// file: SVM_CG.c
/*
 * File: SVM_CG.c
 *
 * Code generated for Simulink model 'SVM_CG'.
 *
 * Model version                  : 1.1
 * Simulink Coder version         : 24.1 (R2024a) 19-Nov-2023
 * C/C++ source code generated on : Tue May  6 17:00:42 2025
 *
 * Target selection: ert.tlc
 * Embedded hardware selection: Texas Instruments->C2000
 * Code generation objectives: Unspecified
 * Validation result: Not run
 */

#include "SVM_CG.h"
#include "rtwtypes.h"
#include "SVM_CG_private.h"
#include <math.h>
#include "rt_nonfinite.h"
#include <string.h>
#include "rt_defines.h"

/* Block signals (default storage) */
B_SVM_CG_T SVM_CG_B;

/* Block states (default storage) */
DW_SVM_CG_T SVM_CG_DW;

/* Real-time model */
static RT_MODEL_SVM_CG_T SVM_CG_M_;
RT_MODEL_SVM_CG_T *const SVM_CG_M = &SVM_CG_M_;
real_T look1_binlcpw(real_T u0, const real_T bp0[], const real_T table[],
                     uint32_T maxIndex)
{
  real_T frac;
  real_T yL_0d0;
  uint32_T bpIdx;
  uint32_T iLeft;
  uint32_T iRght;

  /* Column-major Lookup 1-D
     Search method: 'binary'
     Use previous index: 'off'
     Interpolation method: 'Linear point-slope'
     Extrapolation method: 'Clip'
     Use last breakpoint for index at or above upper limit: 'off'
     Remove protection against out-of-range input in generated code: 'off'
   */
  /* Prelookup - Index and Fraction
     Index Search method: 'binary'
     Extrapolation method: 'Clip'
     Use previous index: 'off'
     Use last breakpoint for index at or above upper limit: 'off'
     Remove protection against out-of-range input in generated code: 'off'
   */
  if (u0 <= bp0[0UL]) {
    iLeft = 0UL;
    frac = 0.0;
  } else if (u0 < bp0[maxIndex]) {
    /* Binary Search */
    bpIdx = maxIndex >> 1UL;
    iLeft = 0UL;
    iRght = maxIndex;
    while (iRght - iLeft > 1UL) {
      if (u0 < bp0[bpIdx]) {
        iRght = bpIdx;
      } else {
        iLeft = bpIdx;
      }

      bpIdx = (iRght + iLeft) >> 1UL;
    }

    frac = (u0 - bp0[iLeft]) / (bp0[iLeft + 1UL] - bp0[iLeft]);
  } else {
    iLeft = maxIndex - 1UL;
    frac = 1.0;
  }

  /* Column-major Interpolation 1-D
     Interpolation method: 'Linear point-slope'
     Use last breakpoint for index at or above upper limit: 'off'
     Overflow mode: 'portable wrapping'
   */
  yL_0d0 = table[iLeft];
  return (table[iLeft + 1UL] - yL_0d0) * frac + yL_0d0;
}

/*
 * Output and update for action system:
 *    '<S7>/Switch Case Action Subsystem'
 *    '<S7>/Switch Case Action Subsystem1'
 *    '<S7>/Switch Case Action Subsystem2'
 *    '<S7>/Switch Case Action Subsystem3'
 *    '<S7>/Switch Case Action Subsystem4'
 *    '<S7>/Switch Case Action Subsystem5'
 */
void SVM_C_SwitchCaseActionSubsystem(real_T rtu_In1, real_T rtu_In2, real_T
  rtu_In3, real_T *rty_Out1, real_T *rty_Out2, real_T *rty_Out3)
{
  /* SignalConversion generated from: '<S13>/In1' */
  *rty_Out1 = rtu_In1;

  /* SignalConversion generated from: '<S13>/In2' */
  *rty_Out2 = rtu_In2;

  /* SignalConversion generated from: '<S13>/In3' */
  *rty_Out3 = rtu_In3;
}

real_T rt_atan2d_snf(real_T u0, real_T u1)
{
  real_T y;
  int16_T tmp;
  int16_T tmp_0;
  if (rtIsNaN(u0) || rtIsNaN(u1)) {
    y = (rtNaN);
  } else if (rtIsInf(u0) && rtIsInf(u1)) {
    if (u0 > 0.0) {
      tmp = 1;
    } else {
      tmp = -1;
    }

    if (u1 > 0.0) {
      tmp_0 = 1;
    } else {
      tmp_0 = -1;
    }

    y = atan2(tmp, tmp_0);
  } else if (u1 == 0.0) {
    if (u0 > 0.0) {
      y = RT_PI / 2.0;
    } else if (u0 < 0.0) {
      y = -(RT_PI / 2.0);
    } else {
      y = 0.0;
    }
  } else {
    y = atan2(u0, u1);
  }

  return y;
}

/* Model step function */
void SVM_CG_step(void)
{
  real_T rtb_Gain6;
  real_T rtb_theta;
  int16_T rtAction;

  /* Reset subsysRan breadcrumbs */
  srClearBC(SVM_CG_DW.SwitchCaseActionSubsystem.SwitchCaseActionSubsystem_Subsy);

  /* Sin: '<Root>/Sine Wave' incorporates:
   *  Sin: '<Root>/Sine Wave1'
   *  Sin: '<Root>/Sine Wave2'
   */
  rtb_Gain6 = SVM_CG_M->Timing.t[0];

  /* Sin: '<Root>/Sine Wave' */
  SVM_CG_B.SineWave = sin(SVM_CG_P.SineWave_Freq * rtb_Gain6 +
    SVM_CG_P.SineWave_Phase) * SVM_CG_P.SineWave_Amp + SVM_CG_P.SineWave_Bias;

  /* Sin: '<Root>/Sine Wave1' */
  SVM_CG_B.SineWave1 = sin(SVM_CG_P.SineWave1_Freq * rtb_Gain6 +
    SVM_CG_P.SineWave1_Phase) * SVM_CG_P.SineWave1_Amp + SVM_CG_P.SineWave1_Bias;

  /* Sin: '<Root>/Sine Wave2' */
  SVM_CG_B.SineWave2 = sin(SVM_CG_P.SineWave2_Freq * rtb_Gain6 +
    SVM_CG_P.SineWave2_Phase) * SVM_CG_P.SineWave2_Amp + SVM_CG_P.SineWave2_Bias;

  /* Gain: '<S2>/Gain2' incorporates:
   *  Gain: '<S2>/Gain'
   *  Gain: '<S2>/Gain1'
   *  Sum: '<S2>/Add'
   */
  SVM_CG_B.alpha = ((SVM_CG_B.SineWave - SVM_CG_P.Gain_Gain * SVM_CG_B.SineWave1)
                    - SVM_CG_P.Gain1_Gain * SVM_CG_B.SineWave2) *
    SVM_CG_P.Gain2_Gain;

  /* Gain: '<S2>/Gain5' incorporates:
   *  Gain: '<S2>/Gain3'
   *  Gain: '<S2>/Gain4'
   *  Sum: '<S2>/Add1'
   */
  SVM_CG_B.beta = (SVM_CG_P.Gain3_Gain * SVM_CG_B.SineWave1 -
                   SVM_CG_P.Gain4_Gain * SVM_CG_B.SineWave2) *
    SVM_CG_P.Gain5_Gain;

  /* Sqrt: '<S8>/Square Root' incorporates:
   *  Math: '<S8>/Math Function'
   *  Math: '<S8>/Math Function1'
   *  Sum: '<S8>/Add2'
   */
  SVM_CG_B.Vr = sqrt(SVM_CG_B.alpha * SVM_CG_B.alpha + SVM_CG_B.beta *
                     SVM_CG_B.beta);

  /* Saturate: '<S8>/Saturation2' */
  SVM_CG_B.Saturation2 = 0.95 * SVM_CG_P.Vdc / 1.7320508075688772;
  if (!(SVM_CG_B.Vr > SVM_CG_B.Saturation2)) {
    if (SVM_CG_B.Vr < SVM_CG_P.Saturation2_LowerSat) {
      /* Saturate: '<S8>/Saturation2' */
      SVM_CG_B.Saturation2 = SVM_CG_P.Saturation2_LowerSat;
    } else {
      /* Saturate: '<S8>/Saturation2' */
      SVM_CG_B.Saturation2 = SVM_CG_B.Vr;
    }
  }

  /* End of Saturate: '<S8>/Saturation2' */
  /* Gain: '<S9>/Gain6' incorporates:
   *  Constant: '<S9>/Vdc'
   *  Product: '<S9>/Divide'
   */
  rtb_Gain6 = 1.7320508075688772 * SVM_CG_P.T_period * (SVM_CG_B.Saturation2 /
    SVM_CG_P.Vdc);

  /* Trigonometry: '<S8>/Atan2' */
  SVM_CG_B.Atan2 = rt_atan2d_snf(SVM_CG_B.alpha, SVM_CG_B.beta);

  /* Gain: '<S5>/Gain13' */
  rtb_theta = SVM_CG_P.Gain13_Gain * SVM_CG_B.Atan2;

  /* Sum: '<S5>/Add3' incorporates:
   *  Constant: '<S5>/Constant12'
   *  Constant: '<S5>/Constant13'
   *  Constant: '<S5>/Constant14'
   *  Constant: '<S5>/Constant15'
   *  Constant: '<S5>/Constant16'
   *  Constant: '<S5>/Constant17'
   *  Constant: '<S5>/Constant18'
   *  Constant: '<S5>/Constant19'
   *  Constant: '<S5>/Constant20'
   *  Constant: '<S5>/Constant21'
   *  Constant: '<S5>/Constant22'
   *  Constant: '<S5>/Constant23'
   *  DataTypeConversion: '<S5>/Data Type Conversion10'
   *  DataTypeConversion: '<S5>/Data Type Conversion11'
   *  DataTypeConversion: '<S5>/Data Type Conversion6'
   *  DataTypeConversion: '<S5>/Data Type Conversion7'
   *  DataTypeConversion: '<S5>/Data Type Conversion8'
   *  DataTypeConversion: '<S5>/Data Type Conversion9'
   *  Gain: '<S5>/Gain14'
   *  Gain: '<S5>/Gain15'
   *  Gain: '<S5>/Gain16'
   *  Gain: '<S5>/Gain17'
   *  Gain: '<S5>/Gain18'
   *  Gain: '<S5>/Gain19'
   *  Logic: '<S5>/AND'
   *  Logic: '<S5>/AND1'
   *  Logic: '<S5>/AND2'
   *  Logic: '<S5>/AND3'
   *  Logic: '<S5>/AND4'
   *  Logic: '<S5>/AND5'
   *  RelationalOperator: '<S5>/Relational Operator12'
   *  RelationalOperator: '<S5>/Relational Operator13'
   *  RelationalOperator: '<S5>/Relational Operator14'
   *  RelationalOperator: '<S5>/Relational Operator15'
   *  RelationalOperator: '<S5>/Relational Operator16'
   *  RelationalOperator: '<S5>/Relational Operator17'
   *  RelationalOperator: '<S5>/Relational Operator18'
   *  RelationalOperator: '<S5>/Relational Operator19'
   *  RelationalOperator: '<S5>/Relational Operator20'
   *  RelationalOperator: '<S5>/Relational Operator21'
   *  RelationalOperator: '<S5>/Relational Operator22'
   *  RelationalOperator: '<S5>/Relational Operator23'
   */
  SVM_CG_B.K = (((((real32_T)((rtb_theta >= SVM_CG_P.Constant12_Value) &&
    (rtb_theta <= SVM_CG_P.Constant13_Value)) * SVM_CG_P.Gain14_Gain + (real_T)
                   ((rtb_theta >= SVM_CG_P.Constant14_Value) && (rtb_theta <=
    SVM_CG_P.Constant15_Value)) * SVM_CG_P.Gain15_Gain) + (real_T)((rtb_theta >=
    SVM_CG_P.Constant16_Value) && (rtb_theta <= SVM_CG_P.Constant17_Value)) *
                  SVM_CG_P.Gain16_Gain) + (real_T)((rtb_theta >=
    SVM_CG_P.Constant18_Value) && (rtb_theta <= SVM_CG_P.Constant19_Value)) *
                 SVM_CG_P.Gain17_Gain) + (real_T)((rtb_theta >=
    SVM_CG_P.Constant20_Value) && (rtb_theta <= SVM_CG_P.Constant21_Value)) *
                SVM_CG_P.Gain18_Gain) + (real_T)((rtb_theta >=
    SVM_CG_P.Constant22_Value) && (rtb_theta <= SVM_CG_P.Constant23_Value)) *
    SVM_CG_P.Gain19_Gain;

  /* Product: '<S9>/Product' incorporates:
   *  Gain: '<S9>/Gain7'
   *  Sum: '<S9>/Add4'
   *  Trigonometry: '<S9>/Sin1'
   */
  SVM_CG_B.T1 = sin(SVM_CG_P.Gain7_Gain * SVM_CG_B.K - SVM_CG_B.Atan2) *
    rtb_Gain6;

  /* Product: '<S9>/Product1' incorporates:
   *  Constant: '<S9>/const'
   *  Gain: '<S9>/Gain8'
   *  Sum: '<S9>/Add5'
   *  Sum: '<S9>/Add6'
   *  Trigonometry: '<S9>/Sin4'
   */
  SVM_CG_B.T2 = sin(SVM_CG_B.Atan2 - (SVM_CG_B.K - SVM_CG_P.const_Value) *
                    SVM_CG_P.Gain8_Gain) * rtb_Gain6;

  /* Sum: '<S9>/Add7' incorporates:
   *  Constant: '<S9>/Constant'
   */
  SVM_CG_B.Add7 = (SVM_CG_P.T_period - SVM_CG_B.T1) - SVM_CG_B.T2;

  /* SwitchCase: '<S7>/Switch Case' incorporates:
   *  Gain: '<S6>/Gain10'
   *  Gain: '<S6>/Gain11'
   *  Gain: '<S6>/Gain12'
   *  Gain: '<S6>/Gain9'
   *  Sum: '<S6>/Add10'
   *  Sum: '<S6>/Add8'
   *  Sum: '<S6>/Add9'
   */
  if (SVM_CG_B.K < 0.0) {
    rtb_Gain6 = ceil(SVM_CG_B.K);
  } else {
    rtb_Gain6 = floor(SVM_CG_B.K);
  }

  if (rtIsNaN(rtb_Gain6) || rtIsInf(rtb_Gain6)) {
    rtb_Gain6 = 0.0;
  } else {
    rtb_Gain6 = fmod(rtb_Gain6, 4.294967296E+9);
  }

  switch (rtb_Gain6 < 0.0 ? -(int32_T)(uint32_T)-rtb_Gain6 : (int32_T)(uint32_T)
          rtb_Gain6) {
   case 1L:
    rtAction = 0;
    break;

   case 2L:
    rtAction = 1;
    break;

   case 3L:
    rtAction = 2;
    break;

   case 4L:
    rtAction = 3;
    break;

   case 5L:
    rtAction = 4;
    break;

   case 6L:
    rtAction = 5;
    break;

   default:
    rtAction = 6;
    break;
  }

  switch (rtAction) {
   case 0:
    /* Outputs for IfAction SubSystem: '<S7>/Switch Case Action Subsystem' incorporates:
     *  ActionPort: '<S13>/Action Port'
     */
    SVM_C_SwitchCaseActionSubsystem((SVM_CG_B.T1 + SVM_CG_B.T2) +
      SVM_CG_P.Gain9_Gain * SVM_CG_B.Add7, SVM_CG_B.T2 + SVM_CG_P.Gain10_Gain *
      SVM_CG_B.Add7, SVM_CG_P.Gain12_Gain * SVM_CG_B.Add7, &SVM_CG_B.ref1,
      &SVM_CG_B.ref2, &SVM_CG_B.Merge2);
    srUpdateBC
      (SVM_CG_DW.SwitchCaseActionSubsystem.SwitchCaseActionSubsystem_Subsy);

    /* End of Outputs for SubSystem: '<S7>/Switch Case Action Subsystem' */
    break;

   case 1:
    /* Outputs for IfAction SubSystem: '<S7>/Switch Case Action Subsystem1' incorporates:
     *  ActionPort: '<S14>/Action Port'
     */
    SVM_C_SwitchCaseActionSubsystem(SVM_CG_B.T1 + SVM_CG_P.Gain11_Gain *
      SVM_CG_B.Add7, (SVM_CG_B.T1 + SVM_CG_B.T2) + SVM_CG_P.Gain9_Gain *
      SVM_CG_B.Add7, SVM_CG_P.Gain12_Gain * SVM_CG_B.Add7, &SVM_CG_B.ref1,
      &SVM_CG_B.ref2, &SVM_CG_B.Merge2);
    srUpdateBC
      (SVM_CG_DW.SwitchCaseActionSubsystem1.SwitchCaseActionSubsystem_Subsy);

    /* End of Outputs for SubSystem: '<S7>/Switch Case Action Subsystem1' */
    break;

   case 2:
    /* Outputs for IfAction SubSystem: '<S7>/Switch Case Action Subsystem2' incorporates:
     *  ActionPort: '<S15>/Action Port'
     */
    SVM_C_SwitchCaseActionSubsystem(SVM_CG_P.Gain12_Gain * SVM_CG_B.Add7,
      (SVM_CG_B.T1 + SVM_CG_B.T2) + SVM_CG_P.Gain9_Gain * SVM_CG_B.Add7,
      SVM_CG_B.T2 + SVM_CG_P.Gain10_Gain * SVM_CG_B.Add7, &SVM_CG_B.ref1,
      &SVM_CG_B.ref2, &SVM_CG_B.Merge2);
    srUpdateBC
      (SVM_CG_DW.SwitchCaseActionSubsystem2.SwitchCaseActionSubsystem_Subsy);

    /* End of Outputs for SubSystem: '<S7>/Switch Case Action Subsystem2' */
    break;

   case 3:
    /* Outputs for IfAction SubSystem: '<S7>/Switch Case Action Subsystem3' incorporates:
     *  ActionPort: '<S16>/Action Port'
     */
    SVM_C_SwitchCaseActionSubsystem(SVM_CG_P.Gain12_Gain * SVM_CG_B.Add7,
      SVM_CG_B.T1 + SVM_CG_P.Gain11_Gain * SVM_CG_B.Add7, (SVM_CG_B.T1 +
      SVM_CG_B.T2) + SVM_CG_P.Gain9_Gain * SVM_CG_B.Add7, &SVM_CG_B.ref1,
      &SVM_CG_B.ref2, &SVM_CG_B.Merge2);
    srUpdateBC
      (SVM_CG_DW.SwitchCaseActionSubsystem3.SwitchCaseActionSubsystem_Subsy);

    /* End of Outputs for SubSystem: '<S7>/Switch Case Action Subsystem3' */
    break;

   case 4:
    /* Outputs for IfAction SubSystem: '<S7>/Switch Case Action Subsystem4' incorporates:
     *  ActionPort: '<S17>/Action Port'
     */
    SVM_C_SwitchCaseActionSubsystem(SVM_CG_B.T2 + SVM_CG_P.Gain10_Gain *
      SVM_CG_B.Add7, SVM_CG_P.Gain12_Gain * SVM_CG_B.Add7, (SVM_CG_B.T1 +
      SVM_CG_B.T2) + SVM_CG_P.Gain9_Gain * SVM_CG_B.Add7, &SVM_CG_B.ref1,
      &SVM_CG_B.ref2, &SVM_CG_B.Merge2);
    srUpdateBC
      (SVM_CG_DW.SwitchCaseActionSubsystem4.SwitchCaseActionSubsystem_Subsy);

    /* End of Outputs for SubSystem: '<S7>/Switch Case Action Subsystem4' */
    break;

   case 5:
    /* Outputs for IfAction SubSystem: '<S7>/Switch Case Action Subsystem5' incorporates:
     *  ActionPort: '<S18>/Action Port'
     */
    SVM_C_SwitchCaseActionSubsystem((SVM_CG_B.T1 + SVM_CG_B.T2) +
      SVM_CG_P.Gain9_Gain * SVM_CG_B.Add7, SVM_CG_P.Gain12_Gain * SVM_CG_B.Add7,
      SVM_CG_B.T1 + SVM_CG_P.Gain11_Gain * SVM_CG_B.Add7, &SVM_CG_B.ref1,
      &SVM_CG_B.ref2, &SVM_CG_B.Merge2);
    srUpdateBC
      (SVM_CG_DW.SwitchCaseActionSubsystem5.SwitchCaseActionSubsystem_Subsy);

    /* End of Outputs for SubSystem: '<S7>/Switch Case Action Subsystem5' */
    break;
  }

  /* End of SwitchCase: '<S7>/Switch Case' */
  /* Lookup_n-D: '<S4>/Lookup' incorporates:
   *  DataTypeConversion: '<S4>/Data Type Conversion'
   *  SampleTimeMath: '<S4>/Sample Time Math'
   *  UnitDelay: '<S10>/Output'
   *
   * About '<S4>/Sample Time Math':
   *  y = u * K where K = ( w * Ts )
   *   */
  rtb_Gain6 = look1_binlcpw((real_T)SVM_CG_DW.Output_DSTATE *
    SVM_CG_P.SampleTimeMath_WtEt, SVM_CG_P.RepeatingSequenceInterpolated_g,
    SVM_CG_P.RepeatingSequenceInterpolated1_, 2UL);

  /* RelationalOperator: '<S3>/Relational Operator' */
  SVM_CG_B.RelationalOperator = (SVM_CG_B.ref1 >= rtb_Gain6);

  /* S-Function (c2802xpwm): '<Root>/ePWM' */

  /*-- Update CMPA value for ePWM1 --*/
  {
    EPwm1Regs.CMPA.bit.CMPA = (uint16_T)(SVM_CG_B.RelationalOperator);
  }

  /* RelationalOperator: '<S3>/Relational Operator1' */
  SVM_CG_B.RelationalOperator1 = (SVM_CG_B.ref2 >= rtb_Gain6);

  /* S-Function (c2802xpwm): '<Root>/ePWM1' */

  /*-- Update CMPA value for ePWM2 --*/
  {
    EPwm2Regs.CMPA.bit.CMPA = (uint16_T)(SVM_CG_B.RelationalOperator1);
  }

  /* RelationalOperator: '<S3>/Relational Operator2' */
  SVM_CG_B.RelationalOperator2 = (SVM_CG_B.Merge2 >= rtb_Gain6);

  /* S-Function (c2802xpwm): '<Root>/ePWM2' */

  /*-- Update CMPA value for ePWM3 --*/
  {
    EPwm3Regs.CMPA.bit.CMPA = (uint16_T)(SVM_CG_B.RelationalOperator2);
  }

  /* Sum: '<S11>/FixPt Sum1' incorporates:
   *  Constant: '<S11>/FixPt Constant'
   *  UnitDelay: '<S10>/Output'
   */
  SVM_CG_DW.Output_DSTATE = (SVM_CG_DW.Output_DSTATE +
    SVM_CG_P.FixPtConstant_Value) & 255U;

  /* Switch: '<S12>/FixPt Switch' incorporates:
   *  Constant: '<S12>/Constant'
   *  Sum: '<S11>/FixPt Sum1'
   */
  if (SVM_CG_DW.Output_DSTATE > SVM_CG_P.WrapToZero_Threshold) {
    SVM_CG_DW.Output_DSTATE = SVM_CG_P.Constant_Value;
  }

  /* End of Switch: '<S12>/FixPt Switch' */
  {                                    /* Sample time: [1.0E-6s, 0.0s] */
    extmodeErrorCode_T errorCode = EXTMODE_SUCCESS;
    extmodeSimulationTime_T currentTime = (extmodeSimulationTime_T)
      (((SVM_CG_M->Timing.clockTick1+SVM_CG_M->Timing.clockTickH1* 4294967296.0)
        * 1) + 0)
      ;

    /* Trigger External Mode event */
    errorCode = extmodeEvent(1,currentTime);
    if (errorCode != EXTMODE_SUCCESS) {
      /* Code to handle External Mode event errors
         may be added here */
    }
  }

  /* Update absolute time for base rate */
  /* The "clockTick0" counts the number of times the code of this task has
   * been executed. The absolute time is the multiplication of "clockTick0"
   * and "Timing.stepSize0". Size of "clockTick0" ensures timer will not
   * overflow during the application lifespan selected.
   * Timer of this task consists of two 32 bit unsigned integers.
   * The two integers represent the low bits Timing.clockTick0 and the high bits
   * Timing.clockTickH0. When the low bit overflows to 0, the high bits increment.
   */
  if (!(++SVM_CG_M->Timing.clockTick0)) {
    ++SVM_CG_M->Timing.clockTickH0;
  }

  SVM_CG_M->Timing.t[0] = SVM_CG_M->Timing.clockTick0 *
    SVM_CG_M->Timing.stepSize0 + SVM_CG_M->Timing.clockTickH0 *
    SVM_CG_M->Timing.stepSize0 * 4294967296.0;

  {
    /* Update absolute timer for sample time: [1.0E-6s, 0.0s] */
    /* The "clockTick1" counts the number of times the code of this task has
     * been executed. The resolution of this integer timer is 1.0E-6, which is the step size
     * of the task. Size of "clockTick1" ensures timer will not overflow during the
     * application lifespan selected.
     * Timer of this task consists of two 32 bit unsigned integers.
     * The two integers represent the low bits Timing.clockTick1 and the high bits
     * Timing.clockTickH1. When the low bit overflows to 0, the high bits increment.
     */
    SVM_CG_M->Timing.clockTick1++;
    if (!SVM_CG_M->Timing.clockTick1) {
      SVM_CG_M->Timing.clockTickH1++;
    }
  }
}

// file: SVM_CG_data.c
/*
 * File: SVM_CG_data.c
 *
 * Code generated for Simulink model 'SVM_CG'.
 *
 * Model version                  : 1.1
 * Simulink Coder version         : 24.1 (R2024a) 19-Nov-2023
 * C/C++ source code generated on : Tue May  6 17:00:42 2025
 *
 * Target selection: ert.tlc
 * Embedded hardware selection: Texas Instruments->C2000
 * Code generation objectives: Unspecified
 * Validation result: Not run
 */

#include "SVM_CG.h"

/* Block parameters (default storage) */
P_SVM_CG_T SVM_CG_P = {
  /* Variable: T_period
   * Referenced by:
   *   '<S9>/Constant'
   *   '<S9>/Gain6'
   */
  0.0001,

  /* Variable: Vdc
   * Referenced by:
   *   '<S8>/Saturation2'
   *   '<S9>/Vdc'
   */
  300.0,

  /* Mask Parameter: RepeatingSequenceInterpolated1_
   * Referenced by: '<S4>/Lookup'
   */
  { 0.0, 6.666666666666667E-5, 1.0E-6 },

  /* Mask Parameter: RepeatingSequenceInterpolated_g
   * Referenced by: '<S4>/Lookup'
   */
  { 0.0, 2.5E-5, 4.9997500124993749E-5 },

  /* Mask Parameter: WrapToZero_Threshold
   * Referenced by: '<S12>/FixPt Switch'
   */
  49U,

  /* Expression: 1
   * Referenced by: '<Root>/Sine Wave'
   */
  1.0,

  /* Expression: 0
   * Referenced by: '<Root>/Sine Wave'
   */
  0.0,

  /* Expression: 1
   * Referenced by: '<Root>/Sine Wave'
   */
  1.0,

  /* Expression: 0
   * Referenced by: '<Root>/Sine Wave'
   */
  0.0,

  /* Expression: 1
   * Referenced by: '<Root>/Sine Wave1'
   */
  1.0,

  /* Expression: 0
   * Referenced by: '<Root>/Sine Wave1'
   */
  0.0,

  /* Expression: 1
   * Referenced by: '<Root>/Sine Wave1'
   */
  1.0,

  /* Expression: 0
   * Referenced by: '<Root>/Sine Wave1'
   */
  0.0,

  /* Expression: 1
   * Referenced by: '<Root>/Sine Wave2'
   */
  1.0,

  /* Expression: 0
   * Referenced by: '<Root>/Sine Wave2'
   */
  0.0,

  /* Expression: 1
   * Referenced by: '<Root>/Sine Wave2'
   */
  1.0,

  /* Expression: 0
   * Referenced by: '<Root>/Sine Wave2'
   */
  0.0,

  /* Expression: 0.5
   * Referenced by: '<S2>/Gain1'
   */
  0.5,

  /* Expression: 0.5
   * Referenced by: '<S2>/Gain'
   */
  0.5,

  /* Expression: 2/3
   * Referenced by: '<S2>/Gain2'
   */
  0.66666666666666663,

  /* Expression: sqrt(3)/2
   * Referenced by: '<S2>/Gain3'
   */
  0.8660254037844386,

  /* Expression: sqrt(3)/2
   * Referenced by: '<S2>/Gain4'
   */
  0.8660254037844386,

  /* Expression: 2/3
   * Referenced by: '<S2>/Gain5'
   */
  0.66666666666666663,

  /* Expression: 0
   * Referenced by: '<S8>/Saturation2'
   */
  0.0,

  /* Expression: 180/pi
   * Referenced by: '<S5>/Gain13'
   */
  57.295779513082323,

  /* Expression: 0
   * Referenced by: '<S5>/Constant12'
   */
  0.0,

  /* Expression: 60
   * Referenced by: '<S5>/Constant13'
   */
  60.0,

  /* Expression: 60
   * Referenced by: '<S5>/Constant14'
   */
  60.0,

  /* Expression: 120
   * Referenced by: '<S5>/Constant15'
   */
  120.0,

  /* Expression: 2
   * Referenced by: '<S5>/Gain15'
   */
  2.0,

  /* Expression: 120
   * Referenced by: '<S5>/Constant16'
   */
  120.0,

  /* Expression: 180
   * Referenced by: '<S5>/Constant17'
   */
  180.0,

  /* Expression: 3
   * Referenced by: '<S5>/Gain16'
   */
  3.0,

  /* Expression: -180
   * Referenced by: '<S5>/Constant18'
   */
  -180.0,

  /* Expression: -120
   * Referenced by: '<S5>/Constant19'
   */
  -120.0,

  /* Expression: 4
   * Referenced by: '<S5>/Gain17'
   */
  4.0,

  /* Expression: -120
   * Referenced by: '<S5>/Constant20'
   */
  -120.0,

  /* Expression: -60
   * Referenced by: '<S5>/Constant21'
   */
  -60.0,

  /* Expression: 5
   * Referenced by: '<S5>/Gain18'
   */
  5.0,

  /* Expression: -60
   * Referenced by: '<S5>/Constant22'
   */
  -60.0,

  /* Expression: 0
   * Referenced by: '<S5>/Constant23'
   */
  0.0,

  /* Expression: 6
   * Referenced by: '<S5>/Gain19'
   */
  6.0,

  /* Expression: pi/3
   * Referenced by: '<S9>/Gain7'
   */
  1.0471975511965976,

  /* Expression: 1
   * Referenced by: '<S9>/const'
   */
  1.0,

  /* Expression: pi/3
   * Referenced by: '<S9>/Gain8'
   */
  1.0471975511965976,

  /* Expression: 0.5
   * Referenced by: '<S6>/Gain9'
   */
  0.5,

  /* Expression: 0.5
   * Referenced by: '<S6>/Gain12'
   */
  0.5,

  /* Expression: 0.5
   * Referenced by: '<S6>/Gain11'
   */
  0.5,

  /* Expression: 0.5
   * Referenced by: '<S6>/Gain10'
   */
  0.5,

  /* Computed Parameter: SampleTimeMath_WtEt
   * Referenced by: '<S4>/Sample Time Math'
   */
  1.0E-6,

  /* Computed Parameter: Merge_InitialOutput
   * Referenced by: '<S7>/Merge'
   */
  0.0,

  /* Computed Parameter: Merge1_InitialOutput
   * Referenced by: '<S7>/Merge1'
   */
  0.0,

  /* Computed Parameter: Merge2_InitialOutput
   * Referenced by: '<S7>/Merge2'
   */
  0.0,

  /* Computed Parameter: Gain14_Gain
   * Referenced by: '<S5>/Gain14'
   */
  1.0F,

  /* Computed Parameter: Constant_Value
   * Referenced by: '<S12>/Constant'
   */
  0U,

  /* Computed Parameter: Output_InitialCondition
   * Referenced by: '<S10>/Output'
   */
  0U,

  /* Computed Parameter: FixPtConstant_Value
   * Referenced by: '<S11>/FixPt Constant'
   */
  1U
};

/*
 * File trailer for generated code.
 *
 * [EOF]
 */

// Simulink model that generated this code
simulink model "SVM_CG"  (R2024a)
settings: Solver=FixedStepDiscrete  StartTime=0.0  StopTime=Inf  RelTol=1e-3  EnableMultiTasking=on
undefined symbols (not defined in the file): Down, GPTRIP1SEL, T_period, TZ1, Up, Vdc
libraries: c2802xlib x3, simulink x1

== system SVM_CG ==
  SVPWM : Subsystem
  Sine Wave : Sin  SampleTime=0
  Sine Wave1 : Sin  SampleTime=0
  Sine Wave2 : Sin  SampleTime=0
  ePWM : c2802xlib/ePWM  PwmType=C2000_Type4  useModule=ePWM1  ePWMxLINKTBPRD=Not Linked  periodUnits=Clock cycles  timerSource=Specify via dialog  timerPeriod_clk=10000  timerPeriod_sec=0.0001  tbshadow=Counter equals to zero  countingMode=Up-Down  phaseActiveEnable=Disable  phaseDirection=Count down after sync  phaseActive=0  synchronizationEnable=off  dcaevt1Sync=off  dcbevt1Sync=off  synchronizationOption=Disable  dcbevt1SyncOut=off  dcaevt1SyncOut=off  cmpdSyncOut=off  cmpcSyncOut=off  cmpbSyncOut=off  zeroSyncOut=off  swfSyncOut=off  perSynchronizationOption=Counter equals to period (CTR=PRD)  clockPrescale=1  HSclockPrescale=1  enswap=off  ePWMxAStatus=on  ePWMxAactionLogic1=Do nothing  ePWMxAactionLogic2=Do nothing  ePWMxAactionLogic3=Clear  ePWMxAactionLogic4=Set  ePWMxAactionLogic5=Do nothing  ePWMxAactionLogic6=Do nothing  ePWMxACSFenable=off  ePWMxACSFvalue=Forcing disable  ePWMxASFreload=Zero  ePWMxBStatus=on  ePWMxBactionLogic1=Do nothing  ePWMxBactionLogic2=Do nothing  ePWMxBactionLogic3=Set  ePWMxBactionLogic4=Clear  ePWMxBactionLogic5=Do nothing  ePWMxBactionLogic6=Do nothing  ePWMxBCSFenable=off  ePWMxBCSFvalue=Forcing disable  ePWMxBSFreload=Zero  ePWNxBOutWay=off  ePWMxLINKCMPA=Not Linked  CMPAUnits=Clock cycles  CMPASource=Input port  CMPAValue_per=50  CMPAValue_clk=0  enCMPAshadow=Counter equals to zero (CTR=Zero)  ePWMxLINKCMPB=Not Linked  CMPBUnits=Clock cycles  CMPBSource=Specify via dialog  CMPBValue_per=50  CMPBValue_clk=32000  enCMPBshadow=Counter equals to zero (CTR=Zero)  ePWMxLINKCMPC=Not Linked  CMPCUnits=Clock cycles  CMPCSource=Specify via dialog  CMPCValue_per=50  CMPCValue_clk=32000  enCMPCshadow=Counter equals to zero (CTR=Zero)  ePWMxLINKCMPD=Not Linked  CMPDUnits=Clock cycles  CMPDSource=Specify via dialog  CMPDValue_per=50  CMPDValue_clk=32000  enCMPDshadow=Counter equals to zero (CTR=Zero)  enableDBePWMxA=on  enableDBePWMxB=on  enhalfcycle=off  DBpolarity=Active high complementary (AHC)  DBedgeDelay=Positive  DBSource_ePWMxA=ePWMxA  DBSource_ePWMxB=ePWMxA  DBPeriodUnits=Clock cycles  DBperiodSource=Specify via dialog  REDperiod=400  FEDperiod=400  REDperiod_sec=0  FEDperiod_sec=0  LoadModeDBRED=Immediate without using shadow  LoadModeDBFED=Immediate without using shadow  adcstartModuleA=off  adcrequestEventA=First event  adcstartEventA=Digital Compare Module A Event 1 start of conversion (DCAEVT1.soc)  adcstartEventA_type2=Counter equals to zero (CTR=Zero)  adcstartModuleB=off  adcrequestEventB=First event  adcstartEventB=Counter equals to zero (CTR=Zero)  adcstartEventB_type2=Counter equals to zero (CTR=Zero)  intEn=off  intPrd=First event  intSel=Counter equals to zero (CTR=Zero)  intSel_type2=Counter equals to zero (CTR=Zero)  hrpe=off  enHRPWM=off  HRPWM_LoadMode=Counter equals to period (CTR=PRD)  HRPWM_CTLMode=Duty or Period control mode  HRPWM_EDGMode=Both edge  hrpeb=off  enHRPWMB=off  HRPWM_LoadModeB=Counter equals to zero (CTR=ZERO)  HRPWM_CTLModeB=Duty or Period control mode  HRPWM_EDGModeB=Both edge  enHRDBRED=off  enHRDBFED=off  enSFO=on  enautoconv=on  chopperEnable=off  chopperFrequency=1  chopperFirstwidth=1  chopperDuty=12.5%  tripZonesource=Specify via dialog  tzselOSHT1=off  tzselOSHT2=off  tzselOSHT3=off  tzselOSHT4=off  tzselOSHT5=off  tzselOSHT6=off  tzselOSHDCAEV1=off  tzselOSHDCBEV1=off  tzselCBC1=off  tzselCBC2=off  tzselCBC3=off  tzselCBC4=off  tzselCBC5=off  tzselCBC6=off  tzselCBCDCAEV2=off  tzselCBCDCBEV2=off  enTzOstIntr=off  enTzCbcIntr=off  enTzDCAEVT1Intr=off  enTzDCAEVT2Intr=off  enTzDCBEVT1Intr=off  enTzDCBEVT2Intr=off  tzclrCBCLatch=Counter equals to zero (CTR=Zero)  ePWMxAforced=No action  ePWMxBforced=No action  DCAEVT1forced=No action  DCBEVT1forced=No action  DCAEVT2forced=No action  DCBEVT2forced=No action  dcah=Trip Zone 1 input (TZ1)  dcal=Trip Zone 2 input (TZ2)  dcbh=Trip Zone 1 input (TZ1)  dcbl=Trip Zone 2 input (TZ2)  dcah_type2=GPTRIP1SEL/(TZ1)  dcal_type2=GPTRIP1SEL/(TZ1)  dcbh_type2=GPTRIP1SEL/(TZ1)  dcbl_type2=GPTRIP1SEL/(TZ1)  gendcaevt1=Event disabled  gendcaevt2=Event disabled  gendcbevt1=Event disabled  gendcbevt2=Event disabled  dcaevt1src=DCAEVT1 with sync  dcaevt2src=DCAEVT2 with sync  dcbevt1src=DCBEVT1 with sync  dcbevt2src=DCBEVT2 with sync  pulsesel=Counter equals to zero (CTR=Zero)  blankinv=off  blankoffset=0  blankwidth=0  evsrcsel=Filtered version of DCAEVT1 (DCAEVT1FILT)  encape=off
  ePWM1 : c2802xlib/ePWM  PwmType=C2000_Type4  useModule=ePWM2  ePWMxLINKTBPRD=Not Linked  periodUnits=Clock cycles  timerSource=Specify via dialog  timerPeriod_clk=10000  timerPeriod_sec=0.0001  tbshadow=Counter equals to zero  countingMode=Up-Down  phaseActiveEnable=Disable  phaseDirection=Count down after sync  phaseActive=0  synchronizationEnable=off  dcaevt1Sync=off  dcbevt1Sync=off  synchronizationOption=Disable  dcbevt1SyncOut=off  dcaevt1SyncOut=off  cmpdSyncOut=off  cmpcSyncOut=off  cmpbSyncOut=off  zeroSyncOut=off  swfSyncOut=off  perSynchronizationOption=Counter equals to period (CTR=PRD)  clockPrescale=1  HSclockPrescale=1  enswap=off  ePWMxAStatus=on  ePWMxAactionLogic1=Do nothing  ePWMxAactionLogic2=Do nothing  ePWMxAactionLogic3=Clear  ePWMxAactionLogic4=Set  ePWMxAactionLogic5=Do nothing  ePWMxAactionLogic6=Do nothing  ePWMxACSFenable=off  ePWMxACSFvalue=Forcing disable  ePWMxASFreload=Zero  ePWMxBStatus=on  ePWMxBactionLogic1=Do nothing  ePWMxBactionLogic2=Do nothing  ePWMxBactionLogic3=Set  ePWMxBactionLogic4=Clear  ePWMxBactionLogic5=Do nothing  ePWMxBactionLogic6=Do nothing  ePWMxBCSFenable=off  ePWMxBCSFvalue=Forcing disable  ePWMxBSFreload=Zero  ePWNxBOutWay=off  ePWMxLINKCMPA=Not Linked  CMPAUnits=Clock cycles  CMPASource=Input port  CMPAValue_per=50  CMPAValue_clk=0  enCMPAshadow=Counter equals to zero (CTR=Zero)  ePWMxLINKCMPB=Not Linked  CMPBUnits=Clock cycles  CMPBSource=Specify via dialog  CMPBValue_per=50  CMPBValue_clk=32000  enCMPBshadow=Counter equals to zero (CTR=Zero)  ePWMxLINKCMPC=Not Linked  CMPCUnits=Clock cycles  CMPCSource=Specify via dialog  CMPCValue_per=50  CMPCValue_clk=32000  enCMPCshadow=Counter equals to zero (CTR=Zero)  ePWMxLINKCMPD=Not Linked  CMPDUnits=Clock cycles  CMPDSource=Specify via dialog  CMPDValue_per=50  CMPDValue_clk=32000  enCMPDshadow=Counter equals to zero (CTR=Zero)  enableDBePWMxA=on  enableDBePWMxB=on  enhalfcycle=off  DBpolarity=Active high complementary (AHC)  DBedgeDelay=Positive  DBSource_ePWMxA=ePWMxA  DBSource_ePWMxB=ePWMxA  DBPeriodUnits=Clock cycles  DBperiodSource=Specify via dialog  REDperiod=400  FEDperiod=400  REDperiod_sec=0  FEDperiod_sec=0  LoadModeDBRED=Immediate without using shadow  LoadModeDBFED=Immediate without using shadow  adcstartModuleA=off  adcrequestEventA=First event  adcstartEventA=Digital Compare Module A Event 1 start of conversion (DCAEVT1.soc)  adcstartEventA_type2=Counter equals to zero (CTR=Zero)  adcstartModuleB=off  adcrequestEventB=First event  adcstartEventB=Counter equals to zero (CTR=Zero)  adcstartEventB_type2=Counter equals to zero (CTR=Zero)  intEn=off  intPrd=First event  intSel=Counter equals to zero (CTR=Zero)  intSel_type2=Counter equals to zero (CTR=Zero)  hrpe=off  enHRPWM=off  HRPWM_LoadMode=Counter equals to period (CTR=PRD)  HRPWM_CTLMode=Duty or Period control mode  HRPWM_EDGMode=Both edge  hrpeb=off  enHRPWMB=off  HRPWM_LoadModeB=Counter equals to zero (CTR=ZERO)  HRPWM_CTLModeB=Duty or Period control mode  HRPWM_EDGModeB=Both edge  enHRDBRED=off  enHRDBFED=off  enSFO=on  enautoconv=on  chopperEnable=off  chopperFrequency=1  chopperFirstwidth=1  chopperDuty=12.5%  tripZonesource=Specify via dialog  tzselOSHT1=off  tzselOSHT2=off  tzselOSHT3=off  tzselOSHT4=off  tzselOSHT5=off  tzselOSHT6=off  tzselOSHDCAEV1=off  tzselOSHDCBEV1=off  tzselCBC1=off  tzselCBC2=off  tzselCBC3=off  tzselCBC4=off  tzselCBC5=off  tzselCBC6=off  tzselCBCDCAEV2=off  tzselCBCDCBEV2=off  enTzOstIntr=off  enTzCbcIntr=off  enTzDCAEVT1Intr=off  enTzDCAEVT2Intr=off  enTzDCBEVT1Intr=off  enTzDCBEVT2Intr=off  tzclrCBCLatch=Counter equals to zero (CTR=Zero)  ePWMxAforced=No action  ePWMxBforced=No action  DCAEVT1forced=No action  DCBEVT1forced=No action  DCAEVT2forced=No action  DCBEVT2forced=No action  dcah=Trip Zone 1 input (TZ1)  dcal=Trip Zone 2 input (TZ2)  dcbh=Trip Zone 1 input (TZ1)  dcbl=Trip Zone 2 input (TZ2)  dcah_type2=GPTRIP1SEL/(TZ1)  dcal_type2=GPTRIP1SEL/(TZ1)  dcbh_type2=GPTRIP1SEL/(TZ1)  dcbl_type2=GPTRIP1SEL/(TZ1)  gendcaevt1=Event disabled  gendcaevt2=Event disabled  gendcbevt1=Event disabled  gendcbevt2=Event disabled  dcaevt1src=DCAEVT1 with sync  dcaevt2src=DCAEVT2 with sync  dcbevt1src=DCBEVT1 with sync  dcbevt2src=DCBEVT2 with sync  pulsesel=Counter equals to zero (CTR=Zero)  blankinv=off  blankoffset=0  blankwidth=0  evsrcsel=Filtered version of DCAEVT1 (DCAEVT1FILT)  encape=off
  ePWM2 : c2802xlib/ePWM  PwmType=C2000_Type4  useModule=ePWM3  ePWMxLINKTBPRD=Not Linked  periodUnits=Clock cycles  timerSource=Specify via dialog  timerPeriod_clk=10000  timerPeriod_sec=0.0001  tbshadow=Counter equals to zero  countingMode=Up-Down  phaseActiveEnable=Disable  phaseDirection=Count down after sync  phaseActive=0  synchronizationEnable=off  dcaevt1Sync=off  dcbevt1Sync=off  synchronizationOption=Disable  dcbevt1SyncOut=off  dcaevt1SyncOut=off  cmpdSyncOut=off  cmpcSyncOut=off  cmpbSyncOut=off  zeroSyncOut=off  swfSyncOut=off  perSynchronizationOption=Counter equals to period (CTR=PRD)  clockPrescale=1  HSclockPrescale=1  enswap=off  ePWMxAStatus=on  ePWMxAactionLogic1=Do nothing  ePWMxAactionLogic2=Do nothing  ePWMxAactionLogic3=Clear  ePWMxAactionLogic4=Set  ePWMxAactionLogic5=Do nothing  ePWMxAactionLogic6=Do nothing  ePWMxACSFenable=off  ePWMxACSFvalue=Forcing disable  ePWMxASFreload=Zero  ePWMxBStatus=on  ePWMxBactionLogic1=Do nothing  ePWMxBactionLogic2=Do nothing  ePWMxBactionLogic3=Set  ePWMxBactionLogic4=Clear  ePWMxBactionLogic5=Do nothing  ePWMxBactionLogic6=Do nothing  ePWMxBCSFenable=off  ePWMxBCSFvalue=Forcing disable  ePWMxBSFreload=Zero  ePWNxBOutWay=off  ePWMxLINKCMPA=Not Linked  CMPAUnits=Clock cycles  CMPASource=Input port  CMPAValue_per=50  CMPAValue_clk=0  enCMPAshadow=Counter equals to zero (CTR=Zero)  ePWMxLINKCMPB=Not Linked  CMPBUnits=Clock cycles  CMPBSource=Specify via dialog  CMPBValue_per=50  CMPBValue_clk=32000  enCMPBshadow=Counter equals to zero (CTR=Zero)  ePWMxLINKCMPC=Not Linked  CMPCUnits=Clock cycles  CMPCSource=Specify via dialog  CMPCValue_per=50  CMPCValue_clk=32000  enCMPCshadow=Counter equals to zero (CTR=Zero)  ePWMxLINKCMPD=Not Linked  CMPDUnits=Clock cycles  CMPDSource=Specify via dialog  CMPDValue_per=50  CMPDValue_clk=32000  enCMPDshadow=Counter equals to zero (CTR=Zero)  enableDBePWMxA=on  enableDBePWMxB=on  enhalfcycle=off  DBpolarity=Active high complementary (AHC)  DBedgeDelay=Positive  DBSource_ePWMxA=ePWMxA  DBSource_ePWMxB=ePWMxA  DBPeriodUnits=Clock cycles  DBperiodSource=Specify via dialog  REDperiod=400  FEDperiod=400  REDperiod_sec=0  FEDperiod_sec=0  LoadModeDBRED=Immediate without using shadow  LoadModeDBFED=Immediate without using shadow  adcstartModuleA=off  adcrequestEventA=First event  adcstartEventA=Digital Compare Module A Event 1 start of conversion (DCAEVT1.soc)  adcstartEventA_type2=Counter equals to zero (CTR=Zero)  adcstartModuleB=off  adcrequestEventB=First event  adcstartEventB=Counter equals to zero (CTR=Zero)  adcstartEventB_type2=Counter equals to zero (CTR=Zero)  intEn=off  intPrd=First event  intSel=Counter equals to zero (CTR=Zero)  intSel_type2=Counter equals to zero (CTR=Zero)  hrpe=off  enHRPWM=off  HRPWM_LoadMode=Counter equals to period (CTR=PRD)  HRPWM_CTLMode=Duty or Period control mode  HRPWM_EDGMode=Both edge  hrpeb=off  enHRPWMB=off  HRPWM_LoadModeB=Counter equals to zero (CTR=ZERO)  HRPWM_CTLModeB=Duty or Period control mode  HRPWM_EDGModeB=Both edge  enHRDBRED=off  enHRDBFED=off  enSFO=on  enautoconv=on  chopperEnable=off  chopperFrequency=1  chopperFirstwidth=1  chopperDuty=12.5%  tripZonesource=Specify via dialog  tzselOSHT1=off  tzselOSHT2=off  tzselOSHT3=off  tzselOSHT4=off  tzselOSHT5=off  tzselOSHT6=off  tzselOSHDCAEV1=off  tzselOSHDCBEV1=off  tzselCBC1=off  tzselCBC2=off  tzselCBC3=off  tzselCBC4=off  tzselCBC5=off  tzselCBC6=off  tzselCBCDCAEV2=off  tzselCBCDCBEV2=off  enTzOstIntr=off  enTzCbcIntr=off  enTzDCAEVT1Intr=off  enTzDCAEVT2Intr=off  enTzDCBEVT1Intr=off  enTzDCBEVT2Intr=off  tzclrCBCLatch=Counter equals to zero (CTR=Zero)  ePWMxAforced=No action  ePWMxBforced=No action  DCAEVT1forced=No action  DCBEVT1forced=No action  DCAEVT2forced=No action  DCBEVT2forced=No action  dcah=Trip Zone 1 input (TZ1)  dcal=Trip Zone 2 input (TZ2)  dcbh=Trip Zone 1 input (TZ1)  dcbl=Trip Zone 2 input (TZ2)  dcah_type2=GPTRIP1SEL/(TZ1)  dcal_type2=GPTRIP1SEL/(TZ1)  dcbh_type2=GPTRIP1SEL/(TZ1)  dcbl_type2=GPTRIP1SEL/(TZ1)  gendcaevt1=Event disabled  gendcaevt2=Event disabled  gendcbevt1=Event disabled  gendcbevt2=Event disabled  dcaevt1src=DCAEVT1 with sync  dcaevt2src=DCAEVT2 with sync  dcbevt1src=DCBEVT1 with sync  dcbevt2src=DCBEVT2 with sync  pulsesel=Counter equals to zero (CTR=Zero)  blankinv=off  blankoffset=0  blankwidth=0  evsrcsel=Filtered version of DCAEVT1 (DCAEVT1FILT)  encape=off
  wires:
  Sine Wave2/1 -> SVPWM/3(Vc)
  Sine Wave1/1 -> SVPWM/2(Vb)
  Sine Wave/1 -> SVPWM/1(Va)
  SVPWM/3(T5) -> ePWM2/1
  SVPWM/2(T3) -> ePWM1/1
  SVPWM/1(T1) -> ePWM/1

== system SVM_CG/SVPWM ==
  Va : Inport
  Vb : Inport  Port=2
  Vc : Inport  Port=3
  ABC to alpha-beta : Subsystem
  Goto6 : Goto  TagVisibility=global
  PWM : Subsystem
  Repeating Sequence Interpolated1 : simulink/Sources/Repeating Sequence Interpolated  OutValues="[ 0 1/15000  1e-6  ]"  TimeValues=[ 0 1/40000 1/20001]  LookUpMeth=Interpolation-Use End Values  tsamp=1e-6  OutMin=[]  OutMax=[]  OutDataTypeStr=double  OutputDataTypeScalingMode=double  OutDataType=fixdt(0,8)  OutScaling=2^-10
  Scope : Scope  NumInputPorts=3
  Scope1 : Scope  NumInputPorts=3
  Scope2 : Scope  NumInputPorts=3
  Sector selection : Subsystem
  Subsystem3 : Subsystem
  Time equations to Referance signal : Subsystem
  polar form : Subsystem
  time equations : Subsystem
  T1 : Outport
  T3 : Outport  Port=2
  T5 : Outport  Port=3
  tag scope: case1=global, case2=global, case3=global, case4=global
  wires:
  Vb/1 -> ABC to alpha-beta/2(In2)
  time equations/1(T1) -> Scope1/1, Subsystem3/1(In1)
  Va/1 -> ABC to alpha-beta/1(In1)
  Time equations to Referance signal/1(ref1) -> PWM/1(ref1)
  Time equations to Referance signal/2("ref2 ") -> PWM/2(ref2)
  Time equations to Referance signal/3(ref3) -> PWM/3(ref3)
  Vc/1 -> ABC to alpha-beta/3(In3)
  ABC to alpha-beta/1(alpha) -> polar form/1(In1)
  ABC to alpha-beta/2(beta) -> polar form/2(In2)
  PWM/1(PWM1) -> T1/1, Scope2/1
  PWM/2(PWM3) -> T3/1, Scope2/2
  PWM/3(PWM5) -> T5/1, Scope2/3
  polar form/2(Angle) -> Sector selection/1(In1), time equations/3(Angle), Scope/3
  polar form/1(Vr) -> Scope/1, time equations/1(Vref)
  Sector selection/1(K) -> Scope/2, time equations/2(Sector), Goto6/1
  Subsystem3/2(S3) -> [case2]
  Subsystem3/1(S1) -> [case1]
  time equations/3(T0) -> Subsystem3/3(In3), Scope1/3
  time equations/2(T2) -> Scope1/2, Subsystem3/2(In2)
  Subsystem3/4(S5) -> [case4]
  Subsystem3/3(S6) -> [case3]
  Repeating Sequence Interpolated1/1 -> PWM/4(Carrier)

== system SVM_CG/SVPWM/ABC to alpha-beta ==
  In1 : Inport
  In2 : Inport  Port=2
  In3 : Inport  Port=3
  Add : Sum  Inputs=+--
  Add1 : Sum  Inputs=+-
  Gain : Gain  Gain=0.5
  Gain1 : Gain  Gain=0.5
  Gain2 : Gain  Gain=2/3
  Gain3 : Gain  Gain=sqrt(3)/2
  Gain4 : Gain  Gain=sqrt(3)/2
  Gain5 : Gain  Gain=2/3
  Scope1 : Scope  NumInputPorts=3
  alpha : Outport
  beta : Outport  Port=2
  wires:
  Gain3/1 -> Add1/1
  In2/1 -> Gain3/1, Scope1/2, Gain/1
  Gain4/1 -> Add1/2
  Add1/1 -> Gain5/1
  Gain1/1 -> Add/3
  In3/1 -> Scope1/3, Gain4/1, Gain1/1
  Gain/1 -> Add/2
  In1/1 -> Add/1, Scope1/1
  Add/1 -> Gain2/1
  Gain2/1 -> alpha/1  "alpha"
  Gain5/1 -> beta/1  "beta"

== system SVM_CG/SVPWM/PWM ==
  ref1 : Inport
  ref2 : Inport  Port=2
  ref3 : Inport  Port=3
  Carrier : Inport  Port=4
  Relational Operator : RelationalOperator  OutDataTypeStr=boolean  RndMeth=Simplest  InputSameDT=off
  Relational Operator1 : RelationalOperator  OutDataTypeStr=boolean  RndMeth=Simplest  InputSameDT=off
  Relational Operator2 : RelationalOperator  OutDataTypeStr=boolean  RndMeth=Simplest  InputSameDT=off
  PWM1 : Outport
  PWM3 : Outport  Port=2
  PWM5 : Outport  Port=3
  wires:
  ref1/1 -> Relational Operator/1
  ref2/1 -> Relational Operator1/1
  ref3/1 -> Relational Operator2/1
  Carrier/1 -> Relational Operator/2, Relational Operator2/2, Relational Operator1/2
  Relational Operator/1 -> PWM1/1
  Relational Operator1/1 -> PWM3/1
  Relational Operator2/1 -> PWM5/1

== system SVM_CG/SVPWM/Sector selection ==
  In1 : Inport
  AND{,1..5} (6 alike) : Logic  IconShape=distinctive  AllPortsSameDT=off  OutDataTypeStr=boolean
  Add3 : Sum  Inputs=++++++
  Constant12 : Constant  Value=0
  Constant13 : Constant  Value=60
  Constant14 : Constant  Value=60
  Constant15 : Constant  Value=120
  Constant16 : Constant  Value=120
  Constant17 : Constant  Value=180
  Constant18 : Constant  Value=-180
  Constant19 : Constant  Value=-120
  Constant20 : Constant  Value=-120
  Constant21 : Constant  Value=-60
  Constant22 : Constant  Value=-60
  Constant23 : Constant  Value=0
  Data Type Conversion{6..11} (6 alike) : DataTypeConversion  SaturateOnIntegerOverflow=off  RndMeth=Floor
  Gain13 : Gain  Gain=180/pi
  Gain14 : Gain
  Gain15 : Gain  Gain=2
  Gain16 : Gain  Gain=3
  Gain17 : Gain  Gain=4
  Gain18 : Gain  Gain=5
  Gain19 : Gain  Gain=6
  Relational Operator{12,14,16,18,20,22} (6 alike) : RelationalOperator  OutDataTypeStr=boolean  RndMeth=Simplest  InputSameDT=off
  Relational Operator{13,15,17,19,21,23} (6 alike) : RelationalOperator  Operator=<=  OutDataTypeStr=boolean  RndMeth=Simplest  InputSameDT=off
  K : Outport
  wires:
  AND2/1 -> Data Type Conversion8/1
  Relational Operator14/1 -> AND1/1
  Relational Operator12/1 -> AND/1
  Data Type Conversion10/1 -> Gain18/1
  Data Type Conversion8/1 -> Gain16/1
  Relational Operator19/1 -> AND3/2
  Gain13/1 -> Relational Operator14/1, Relational Operator18/1, Relational Operator19/1, Relational Operator20/1, Relational Operator22/1, Relational Operator23/1, Relational Operator21/1, Relational Operator17/1, Relational Operator16/1, Relational Operator15/1, Relational Operator13/1, Relational Operator12/1  "theta"
  Data Type Conversion6/1 -> Gain14/1
  Constant21/1 -> Relational Operator21/2
  Constant19/1 -> Relational Operator19/2
  Gain19/1 -> Add3/6
  Constant18/1 -> Relational Operator18/2
  AND4/1 -> Data Type Conversion10/1
  Constant22/1 -> Relational Operator22/2
  Relational Operator22/1 -> AND5/1
  Relational Operator18/1 -> AND3/1
  Gain15/1 -> Add3/2
  Relational Operator23/1 -> AND5/2
  Data Type Conversion11/1 -> Gain19/1
  Constant16/1 -> Relational Operator16/2
  Data Type Conversion7/1 -> Gain15/1
  Constant23/1 -> Relational Operator23/2
  Relational Operator20/1 -> AND4/1
  Gain18/1 -> Add3/5
  Gain14/1 -> Add3/1
  AND1/1 -> Data Type Conversion7/1
  Constant14/1 -> Relational Operator14/2
  Relational Operator16/1 -> AND2/1
  Relational Operator17/1 -> AND2/2
  Gain17/1 -> Add3/4
  Constant12/1 -> Relational Operator12/2
  Gain16/1 -> Add3/3
  Relational Operator13/1 -> AND/2
  Relational Operator15/1 -> AND1/2
  Data Type Conversion9/1 -> Gain17/1
  AND/1 -> Data Type Conversion6/1
  Constant13/1 -> Relational Operator13/2
  Relational Operator21/1 -> AND4/2
  AND3/1 -> Data Type Conversion9/1
  Constant20/1 -> Relational Operator20/2
  Constant17/1 -> Relational Operator17/2
  AND5/1 -> Data Type Conversion11/1
  Constant15/1 -> Relational Operator15/2
  Add3/1 -> K/1  "K"
  In1/1 -> Gain13/1

== system SVM_CG/SVPWM/Subsystem3 ==
  In1 : Inport
  In2 : Inport  Port=2
  In3 : Inport  Port=3
  Add10 : Sum
  Add8 : Sum  Inputs=+++
  Add9 : Sum
  Gain{9..12} (4 alike) : Gain  Gain=0.5
  S1 : Outport
  S3 : Outport  Port=2
  S6 : Outport  Port=3
  S5 : Outport  Port=4
  wires:
  In3/1 -> Gain9/1, Gain10/1, Gain12/1, Gain11/1
  Gain11/1 -> Add10/2
  Gain9/1 -> Add8/3
  Gain10/1 -> Add9/2
  Add8/1 -> S1/1  "S1"
  In2/1 -> Add9/1, Add8/2
  In1/1 -> Add10/1, Add8/1
  Add9/1 -> S3/1  "S3"
  Gain12/1 -> S5/1  "S5"
  Add10/1 -> S6/1  "S6"

== system SVM_CG/SVPWM/Time equations to Referance signal ==
  From6 : From  TagVisibility=global
  Merge : Merge  Inputs=6
  Merge1 : Merge  Inputs=6
  Merge2 : Merge  Inputs=6
  Switch Case : SwitchCase  CaseConditions={1 2 3 4 5 6}
  Switch Case Action Subsystem : Subsystem  TreatAsAtomicUnit=on
  Switch Case Action Subsystem1 : Subsystem  TreatAsAtomicUnit=on
  Switch Case Action Subsystem2 : Subsystem  TreatAsAtomicUnit=on
  Switch Case Action Subsystem3 : Subsystem  TreatAsAtomicUnit=on
  Switch Case Action Subsystem4 : Subsystem  TreatAsAtomicUnit=on
  Switch Case Action Subsystem5 : Subsystem  TreatAsAtomicUnit=on
  ref1 : Outport
  "ref2 " : Outport  Port=2
  ref3 : Outport  Port=3
  wires:
  [case3] -> Switch Case Action Subsystem5/3(In3)
  Switch Case Action Subsystem4/1(Out1) -> Merge/2
  [case1] -> Switch Case Action Subsystem2/2(In2)
  Switch Case Action Subsystem3/2(Out2) -> Merge1/3
  [case4] -> Switch Case Action Subsystem3/1(In1)
  Switch Case/4 -> Switch Case Action Subsystem3/Action
  [case2] -> Switch Case Action Subsystem4/1(In1)
  Switch Case/6 -> Switch Case Action Subsystem5/Action
  [case4] -> Switch Case Action Subsystem1/3(In3)
  [case1] -> Switch Case Action Subsystem5/1(In1)
  [case3] -> Switch Case Action Subsystem1/1(In1)
  Merge/1 -> ref1/1  "ref1"
  Switch Case Action Subsystem5/1(Out1) -> Merge/1
  Switch Case/5 -> Switch Case Action Subsystem4/Action
  Switch Case Action Subsystem4/3(Out3) -> Merge2/2
  [case1] -> Switch Case Action Subsystem/1(In1)
  Switch Case Action Subsystem2/3(Out3) -> Merge2/4
  Switch Case Action Subsystem4/2(Out2) -> Merge1/2
  Switch Case/3 -> Switch Case Action Subsystem2/Action
  Switch Case Action Subsystem/2(Out2) -> Merge1/6  "ref2"
  Switch Case Action Subsystem3/3(Out3) -> Merge2/3
  Switch Case Action Subsystem5/2(Out2) -> Merge1/1
  [case3] -> Switch Case Action Subsystem3/2(In2)
  Switch Case/2 -> Switch Case Action Subsystem1/Action
  Switch Case Action Subsystem2/1(Out1) -> Merge/4
  Switch Case Action Subsystem2/2(Out2) -> Merge1/4
  [case1] -> Switch Case Action Subsystem4/3(In3)
  [case4] -> Switch Case Action Subsystem5/2(In2)
  Switch Case/1 -> Switch Case Action Subsystem/Action
  Switch Case Action Subsystem5/3(Out3) -> Merge2/1
  [case4] -> Switch Case Action Subsystem2/1(In1)
  Switch Case Action Subsystem3/1(Out1) -> Merge/3
  [case4] -> Switch Case Action Subsystem/3(In3)
  Merge2/1 -> ref3/1
  From6/1 -> Switch Case/1
  [case4] -> Switch Case Action Subsystem4/2(In2)
  [case2] -> Switch Case Action Subsystem/2(In2)
  [case2] -> Switch Case Action Subsystem2/3(In3)
  [case1] -> Switch Case Action Subsystem3/3(In3)
  Switch Case Action Subsystem1/2(Out2) -> Merge1/5
  Switch Case Action Subsystem/1(Out1) -> Merge/6  "ref1"
  Switch Case Action Subsystem1/1(Out1) -> Merge/5
  Switch Case Action Subsystem/3(Out3) -> Merge2/6  "ref3"
  Switch Case Action Subsystem1/3(Out3) -> Merge2/5
  [case1] -> Switch Case Action Subsystem1/2(In2)
  Merge1/1 -> "ref2 "/1  "ref2"

== system SVM_CG/SVPWM/polar form ==
  In1 : Inport
  In2 : Inport  Port=2
  Add2 : Sum
  Atan2 : Trigonometry  Operator=atan2
  Math Function : Math  Operator=square  SignedPower=on
  Math Function1 : Math  Operator=square  SignedPower=on
  Saturation2 : Saturate  UpperLimit=0.95 * Vdc /sqrt(3)  LowerLimit=0
  Scope1 : Scope  NumInputPorts=2
  Scope2 : Scope  NumInputPorts=2
  Square Root : Sqrt
  Vr : Outport
  Angle : Outport  Port=2
  wires:
  In2/1 -> Scope2/2, Atan2/2, Math Function1/1
  In1/1 -> Scope2/1, Atan2/1, Math Function/1
  Math Function1/1 -> Add2/2
  Add2/1 -> Square Root/1
  Math Function/1 -> Add2/1
  Atan2/1 -> Angle/1
  Square Root/1 -> Saturation2/1, Scope1/1  "Vr"
  Saturation2/1 -> Vr/1, Scope1/2

== system SVM_CG/SVPWM/time equations ==
  Vref : Inport
  Sector : Inport  Port=2
  Angle : Inport  Port=3
  Add4 : Sum  Inputs=+-
  Add5 : Sum  Inputs=+-
  Add6 : Sum  Inputs=+-
  Add7 : Sum  Inputs=+--
  Constant : Constant  Value=T_period
  Divide : Product  Inputs=*/
  Gain6 : Gain  Gain=sqrt(3)*(T_period)
  Gain7 : Gain  Gain=pi/3
  Gain8 : Gain  Gain=pi/3
  Product : Product
  Product1 : Product
  Sin1 : Trigonometry
  Sin4 : Trigonometry
  Vdc : Constant  Value=Vdc
  const : Constant
  T1 : Outport
  T2 : Outport  Port=2
  T0 : Outport  Port=3
  wires:
  Vdc/1 -> Divide/2
  Gain6/1 -> Product1/1, Product/1
  Divide/1 -> Gain6/1
  Add6/1 -> Gain8/1
  Constant/1 -> Add7/1
  Gain7/1 -> Add4/1
  Add5/1 -> Sin4/1
  Sin4/1 -> Product1/2
  Sin1/1 -> Product/2
  Gain8/1 -> Add5/2
  Angle/1 -> Add5/1, Add4/2
  const/1 -> Add6/2
  Product1/1 -> T2/1, Add7/3  "T2"
  Sector/1 -> Gain7/1, Add6/1
  Add4/1 -> Sin1/1
  Vref/1 -> Divide/1
  Product/1 -> Add7/2, T1/1  "T1"
  Add7/1 -> T0/1

== system SVM_CG/SVPWM/Time equations to Referance signal/Switch Case Action Subsystem ==
  In1 : Inport
  In2 : Inport  Port=2
  In3 : Inport  Port=3
  Action Port : ActionPort  ActionPortLabel=case [ 1 ]:
  Out1 : Outport
  Out2 : Outport  Port=2
  Out3 : Outport  Port=3
  wires:
  In1/1 -> Out1/1
  In2/1 -> Out2/1
  In3/1 -> Out3/1

== system SVM_CG/SVPWM/Time equations to Referance signal/Switch Case Action Subsystem1 ==
  In1 : Inport
  In2 : Inport  Port=2
  In3 : Inport  Port=3
  Action Port : ActionPort  ActionPortLabel=case [ 2 ]:
  Out1 : Outport
  Out2 : Outport  Port=2
  Out3 : Outport  Port=3
  wires:
  In1/1 -> Out1/1
  In2/1 -> Out2/1
  In3/1 -> Out3/1

== system SVM_CG/SVPWM/Time equations to Referance signal/Switch Case Action Subsystem2 ==
  In1 : Inport
  In2 : Inport  Port=2
  In3 : Inport  Port=3
  Action Port : ActionPort  ActionPortLabel=case [ 3 ]:
  Out1 : Outport
  Out2 : Outport  Port=2
  Out3 : Outport  Port=3
  wires:
  In1/1 -> Out1/1
  In2/1 -> Out2/1
  In3/1 -> Out3/1

== system SVM_CG/SVPWM/Time equations to Referance signal/Switch Case Action Subsystem3 ==
  In1 : Inport
  In2 : Inport  Port=2
  In3 : Inport  Port=3
  Action Port : ActionPort  ActionPortLabel=case [ 4 ]:
  Out1 : Outport
  Out2 : Outport  Port=2
  Out3 : Outport  Port=3
  wires:
  In1/1 -> Out1/1
  In2/1 -> Out2/1
  In3/1 -> Out3/1

== system SVM_CG/SVPWM/Time equations to Referance signal/Switch Case Action Subsystem4 ==
  In1 : Inport
  In2 : Inport  Port=2
  In3 : Inport  Port=3
  Action Port : ActionPort  ActionPortLabel=case [ 5 ]:
  Out1 : Outport
  Out2 : Outport  Port=2
  Out3 : Outport  Port=3
  wires:
  In1/1 -> Out1/1
  In2/1 -> Out2/1
  In3/1 -> Out3/1

== system SVM_CG/SVPWM/Time equations to Referance signal/Switch Case Action Subsystem5 ==
  In1 : Inport
  In2 : Inport  Port=2
  In3 : Inport  Port=3
  Action Port : ActionPort  ActionPortLabel=case [ 6 ]:
  Out1 : Outport
  Out2 : Outport  Port=2
  Out3 : Outport  Port=3
  wires:
  In1/1 -> Out1/1
  In2/1 -> Out2/1
  In3/1 -> Out3/1
